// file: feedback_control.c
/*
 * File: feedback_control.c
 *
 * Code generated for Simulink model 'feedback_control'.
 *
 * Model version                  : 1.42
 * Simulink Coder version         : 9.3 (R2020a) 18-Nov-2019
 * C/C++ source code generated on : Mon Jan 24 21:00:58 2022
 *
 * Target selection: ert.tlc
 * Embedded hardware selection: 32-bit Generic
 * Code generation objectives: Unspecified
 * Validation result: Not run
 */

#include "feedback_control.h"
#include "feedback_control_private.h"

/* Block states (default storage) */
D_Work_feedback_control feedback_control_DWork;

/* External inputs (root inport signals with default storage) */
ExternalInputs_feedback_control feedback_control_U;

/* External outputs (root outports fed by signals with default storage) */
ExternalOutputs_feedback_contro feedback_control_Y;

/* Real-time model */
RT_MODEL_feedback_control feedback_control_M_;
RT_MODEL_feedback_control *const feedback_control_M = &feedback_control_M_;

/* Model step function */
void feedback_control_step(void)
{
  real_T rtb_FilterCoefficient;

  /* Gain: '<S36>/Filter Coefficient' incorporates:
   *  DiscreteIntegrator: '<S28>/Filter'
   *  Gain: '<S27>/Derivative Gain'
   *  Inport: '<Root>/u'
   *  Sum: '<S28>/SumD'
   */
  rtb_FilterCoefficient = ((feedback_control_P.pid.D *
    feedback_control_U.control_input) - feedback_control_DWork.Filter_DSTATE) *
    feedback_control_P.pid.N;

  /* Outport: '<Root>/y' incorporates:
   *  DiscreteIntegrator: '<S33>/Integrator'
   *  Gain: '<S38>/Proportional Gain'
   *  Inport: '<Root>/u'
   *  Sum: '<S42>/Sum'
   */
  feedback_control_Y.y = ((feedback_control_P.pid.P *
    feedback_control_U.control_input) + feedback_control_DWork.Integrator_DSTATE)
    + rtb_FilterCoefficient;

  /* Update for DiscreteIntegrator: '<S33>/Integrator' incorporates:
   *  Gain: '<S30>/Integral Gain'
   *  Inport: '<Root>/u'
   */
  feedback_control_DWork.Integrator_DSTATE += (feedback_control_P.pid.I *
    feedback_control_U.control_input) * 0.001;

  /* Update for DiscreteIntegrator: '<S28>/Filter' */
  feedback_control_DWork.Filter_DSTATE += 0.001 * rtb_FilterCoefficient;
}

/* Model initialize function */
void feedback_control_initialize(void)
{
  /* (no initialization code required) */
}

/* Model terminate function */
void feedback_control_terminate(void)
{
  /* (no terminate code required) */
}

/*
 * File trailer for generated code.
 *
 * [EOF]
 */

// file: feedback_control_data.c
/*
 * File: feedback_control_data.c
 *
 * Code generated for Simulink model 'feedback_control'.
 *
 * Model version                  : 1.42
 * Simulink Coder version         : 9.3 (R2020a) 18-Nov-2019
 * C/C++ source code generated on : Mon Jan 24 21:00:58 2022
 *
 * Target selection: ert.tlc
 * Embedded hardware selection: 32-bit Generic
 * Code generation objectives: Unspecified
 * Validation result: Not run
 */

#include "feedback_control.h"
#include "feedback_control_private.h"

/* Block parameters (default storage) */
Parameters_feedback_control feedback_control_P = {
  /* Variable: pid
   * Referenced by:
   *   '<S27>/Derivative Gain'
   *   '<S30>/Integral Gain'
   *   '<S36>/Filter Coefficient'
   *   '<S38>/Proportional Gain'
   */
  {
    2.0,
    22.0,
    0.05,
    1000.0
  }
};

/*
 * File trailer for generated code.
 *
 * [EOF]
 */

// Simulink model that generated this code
simulink model "feedback_control"  (R2020a)
settings: Solver=FixedStepDiscrete  StartTime=0.0  StopTime=10.0  FixedStep=T_sample_control  RelTol=1e-3  EnableMultiTasking=on
undefined symbols (not defined in the file): pid, T_sample_control
libraries: simulink x1

== system feedback_control ==
  note: Copyright 2012-2017 The MathWorks, Inc.
  u : Inport  OutDataTypeStr=double  PortDimensions=1  SampleTime=T_sample_control
  Discrete PID Controller : simulink/Continuous/PID Controller  Controller=PID  Form=Parallel  TimeDomain=Discrete-time  UseExternalTs=off  SampleTime=T_sample_control  IntegratorMethod=Forward Euler  FilterMethod=Forward Euler  ControllerParametersSource=internal  P=pid.P  I=pid.I  D=pid.D  UseFilter=on  N=pid.N  TunerSelectOption=Transfer Function Based (PID Tuner App)  InitialConditionSource=internal  InitialConditionForIntegrator=0  InitialConditionForFilter=0  DifferentiatorICPrevScaledInput=0  ExternalReset=none  TrackingMode=off  Kt=1  LimitOutput=off  UpperSaturationLimit=inf  LowerSaturationLimit=-inf  LinearizeAsGain=off  AntiWindupMode=none  Kb=1  POutMin=[]  POutMax=[]  IOutMin=[]  IOutMax=[]  DOutMin=[]  DOutMax=[]  NOutMin=[]  NOutMax=[]  SumOutMin=[]  SumOutMax=[]  SaturationOutMin=[]  SaturationOutMax=[]  PParamMin=[]  PParamMax=[]  IParamMin=[]  IParamMax=[]  DParamMin=[]  DParamMax=[]  NParamMin=[]  NParamMax=[]  KbParamMin=[]  KbParamMax=[]  KtParamMin=[]  KtParamMax=[]  KbOutMin=[]  KbOutMax=[]  KtOutMin=[]  KtOutMax=[]  IntegratorOutMin=[]  IntegratorOutMax=[]  FilterOutMin=[]  FilterOutMax=[]  SumI1OutMin=[]  SumI1OutMax=[]  SumI2OutMin=[]  SumI2OutMax=[]  SumI3OutMin=[]  SumI3OutMax=[]  SumI4OutMin=[]  SumI4OutMax=[]  SumDOutMin=[]  SumDOutMax=[]  DifferentiatorOutMin=[]  DifferentiatorOutMax=[]  FilterDiffOutCoefMin=[]  FilterDiffOutCoefMax=[]  ReciprocalOutMin=[]  ReciprocalOutMax=[]  SumDenOutMin=[]  SumDenOutMax=[]  SumNumOutMin=[]  SumNumOutMax=[]  DivideOutMin=[]  DivideOutMax=[]  UdiffTsProdOutMin=[]  UdiffTsProdOutMax=[]  NTsProdOutMin=[]  NTsProdOutMax=[]  UintegralTsProdOutMin=[]  UintegralTsProdOutMax=[]  UngainTsProdOutMin=[]  UngainTsProdOutMax=[]  IntegratorContinuousStateAttributes=''  IntegratorStateMustResolveToSignalObject=off  IntegratorRTWStateStorageClass=Auto  FilterContinuousStateAttributes=''  FilterStateMustResolveToSignalObject=off  FilterRTWStateStorageClass=Auto  ParallelPVariant=InternalParameters  IdealPVariant=Disabled  IVariant=InternalParameters  DVariant=InternalParameters  IntegratorVariant=Discrete  SatVariant=Disabled  AWVariant=Passthrough  PCopyVariant=Disabled  TRVariant=Disabled  FdbkBlocksVariant=Forward  IdealPFdbkVariant=Disabled  SatFdbkVariant=Disabled  DerivativeFilterVariant=ForwardEulerFilter  NVariant=InternalParameters  NCopyVariant=Disabled  FilterICVariant=InternalICsFilter  IntegratorICVariant=InternalICs  ExternalResetVariant=Disabled  TRSumVariant=Passthrough  SumFdbkVariant=Disabled  SumVariant=Sum_PID  TsampFilterVariant=InternalTs  TsampNgainVariant=Passthrough  TsampIntegralVariant=Passthrough
  y : Outport  OutDataTypeStr=double  PortDimensions=1  SampleTime=T_sample_control
  wires:
  u/1 -> Discrete PID Controller/1  "control_input"
  Discrete PID Controller/1 -> y/1  "control_output"
